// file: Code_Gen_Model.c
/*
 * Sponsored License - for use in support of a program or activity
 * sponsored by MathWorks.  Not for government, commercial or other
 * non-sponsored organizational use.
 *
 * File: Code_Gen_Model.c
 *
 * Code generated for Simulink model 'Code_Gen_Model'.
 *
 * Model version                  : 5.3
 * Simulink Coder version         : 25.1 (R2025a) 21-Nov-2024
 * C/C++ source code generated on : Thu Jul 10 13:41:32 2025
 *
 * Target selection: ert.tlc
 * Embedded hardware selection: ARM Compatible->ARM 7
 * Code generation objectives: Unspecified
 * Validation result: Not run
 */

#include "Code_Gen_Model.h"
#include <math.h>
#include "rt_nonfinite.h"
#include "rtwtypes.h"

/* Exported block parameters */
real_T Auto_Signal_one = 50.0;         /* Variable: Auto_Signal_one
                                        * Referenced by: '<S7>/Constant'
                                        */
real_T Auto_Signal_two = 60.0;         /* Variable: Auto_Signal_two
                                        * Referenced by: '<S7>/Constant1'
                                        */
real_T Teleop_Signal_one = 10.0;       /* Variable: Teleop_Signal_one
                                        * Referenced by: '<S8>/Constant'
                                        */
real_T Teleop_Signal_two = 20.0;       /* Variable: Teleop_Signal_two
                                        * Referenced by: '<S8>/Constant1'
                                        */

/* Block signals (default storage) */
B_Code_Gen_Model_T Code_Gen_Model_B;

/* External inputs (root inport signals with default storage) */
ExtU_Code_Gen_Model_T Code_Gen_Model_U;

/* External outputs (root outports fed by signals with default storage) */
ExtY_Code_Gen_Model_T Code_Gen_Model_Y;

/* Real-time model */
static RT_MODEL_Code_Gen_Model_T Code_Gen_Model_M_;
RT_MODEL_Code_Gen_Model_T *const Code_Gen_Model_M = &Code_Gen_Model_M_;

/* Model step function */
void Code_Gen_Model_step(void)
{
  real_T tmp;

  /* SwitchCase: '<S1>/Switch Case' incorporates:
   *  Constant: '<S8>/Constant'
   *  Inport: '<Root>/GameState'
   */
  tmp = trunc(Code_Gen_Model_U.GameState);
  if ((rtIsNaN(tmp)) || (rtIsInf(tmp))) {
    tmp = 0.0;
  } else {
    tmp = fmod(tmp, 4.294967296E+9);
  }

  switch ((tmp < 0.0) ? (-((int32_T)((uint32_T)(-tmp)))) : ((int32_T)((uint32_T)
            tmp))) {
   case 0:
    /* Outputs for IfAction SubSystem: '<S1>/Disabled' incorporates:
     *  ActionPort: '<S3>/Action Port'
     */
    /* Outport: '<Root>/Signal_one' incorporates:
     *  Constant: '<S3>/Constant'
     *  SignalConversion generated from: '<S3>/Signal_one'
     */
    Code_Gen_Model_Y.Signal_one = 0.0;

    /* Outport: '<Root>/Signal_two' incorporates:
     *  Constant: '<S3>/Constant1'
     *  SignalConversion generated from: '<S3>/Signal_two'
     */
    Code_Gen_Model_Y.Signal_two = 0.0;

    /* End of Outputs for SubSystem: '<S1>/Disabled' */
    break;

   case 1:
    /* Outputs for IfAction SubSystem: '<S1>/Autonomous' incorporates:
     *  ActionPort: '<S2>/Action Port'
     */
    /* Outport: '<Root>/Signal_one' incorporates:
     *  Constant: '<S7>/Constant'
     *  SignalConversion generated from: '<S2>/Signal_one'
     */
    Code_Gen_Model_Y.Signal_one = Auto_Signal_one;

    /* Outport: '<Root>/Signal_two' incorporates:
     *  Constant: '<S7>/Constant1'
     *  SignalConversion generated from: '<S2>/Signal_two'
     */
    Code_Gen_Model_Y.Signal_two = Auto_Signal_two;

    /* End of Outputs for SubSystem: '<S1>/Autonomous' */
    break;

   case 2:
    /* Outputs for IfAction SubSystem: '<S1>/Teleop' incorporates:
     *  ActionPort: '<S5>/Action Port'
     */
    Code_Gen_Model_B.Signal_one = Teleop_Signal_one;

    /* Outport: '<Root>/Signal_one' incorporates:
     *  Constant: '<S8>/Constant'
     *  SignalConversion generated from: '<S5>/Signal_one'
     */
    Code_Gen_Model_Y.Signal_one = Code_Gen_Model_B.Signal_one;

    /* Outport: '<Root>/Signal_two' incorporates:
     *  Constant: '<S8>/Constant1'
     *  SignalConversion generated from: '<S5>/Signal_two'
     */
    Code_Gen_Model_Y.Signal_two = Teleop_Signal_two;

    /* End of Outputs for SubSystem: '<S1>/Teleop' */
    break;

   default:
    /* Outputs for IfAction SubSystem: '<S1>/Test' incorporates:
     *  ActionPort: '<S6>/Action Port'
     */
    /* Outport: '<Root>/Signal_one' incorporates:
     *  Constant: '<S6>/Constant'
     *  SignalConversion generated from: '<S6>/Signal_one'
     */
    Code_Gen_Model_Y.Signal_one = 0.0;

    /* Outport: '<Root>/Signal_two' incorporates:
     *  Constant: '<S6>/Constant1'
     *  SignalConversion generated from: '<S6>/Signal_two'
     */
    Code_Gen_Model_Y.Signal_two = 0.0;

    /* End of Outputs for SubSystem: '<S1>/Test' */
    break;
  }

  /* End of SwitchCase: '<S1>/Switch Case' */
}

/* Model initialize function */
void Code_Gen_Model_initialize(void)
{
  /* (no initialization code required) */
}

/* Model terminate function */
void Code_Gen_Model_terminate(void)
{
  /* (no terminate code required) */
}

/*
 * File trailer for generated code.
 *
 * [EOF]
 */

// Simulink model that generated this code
simulink model "Code_Gen_Model"  (R2025a)
settings: Solver=FixedStepDiscrete  StartTime=0.0  StopTime=inf  FixedStep=t_sample  RelTol=1e-3

== system Code_Gen_Model ==
  GameState : Inport
  RoboRio Controls : Subsystem  ReferencedSubsystem=RoboRio_Controls_sub
  Signal_one : Outport
  Signal_two : Outport  Port=2
  wires:
  GameState/1 -> RoboRio Controls/1
  RoboRio Controls/1 -> Signal_one/1
  RoboRio Controls/2 -> Signal_two/1
